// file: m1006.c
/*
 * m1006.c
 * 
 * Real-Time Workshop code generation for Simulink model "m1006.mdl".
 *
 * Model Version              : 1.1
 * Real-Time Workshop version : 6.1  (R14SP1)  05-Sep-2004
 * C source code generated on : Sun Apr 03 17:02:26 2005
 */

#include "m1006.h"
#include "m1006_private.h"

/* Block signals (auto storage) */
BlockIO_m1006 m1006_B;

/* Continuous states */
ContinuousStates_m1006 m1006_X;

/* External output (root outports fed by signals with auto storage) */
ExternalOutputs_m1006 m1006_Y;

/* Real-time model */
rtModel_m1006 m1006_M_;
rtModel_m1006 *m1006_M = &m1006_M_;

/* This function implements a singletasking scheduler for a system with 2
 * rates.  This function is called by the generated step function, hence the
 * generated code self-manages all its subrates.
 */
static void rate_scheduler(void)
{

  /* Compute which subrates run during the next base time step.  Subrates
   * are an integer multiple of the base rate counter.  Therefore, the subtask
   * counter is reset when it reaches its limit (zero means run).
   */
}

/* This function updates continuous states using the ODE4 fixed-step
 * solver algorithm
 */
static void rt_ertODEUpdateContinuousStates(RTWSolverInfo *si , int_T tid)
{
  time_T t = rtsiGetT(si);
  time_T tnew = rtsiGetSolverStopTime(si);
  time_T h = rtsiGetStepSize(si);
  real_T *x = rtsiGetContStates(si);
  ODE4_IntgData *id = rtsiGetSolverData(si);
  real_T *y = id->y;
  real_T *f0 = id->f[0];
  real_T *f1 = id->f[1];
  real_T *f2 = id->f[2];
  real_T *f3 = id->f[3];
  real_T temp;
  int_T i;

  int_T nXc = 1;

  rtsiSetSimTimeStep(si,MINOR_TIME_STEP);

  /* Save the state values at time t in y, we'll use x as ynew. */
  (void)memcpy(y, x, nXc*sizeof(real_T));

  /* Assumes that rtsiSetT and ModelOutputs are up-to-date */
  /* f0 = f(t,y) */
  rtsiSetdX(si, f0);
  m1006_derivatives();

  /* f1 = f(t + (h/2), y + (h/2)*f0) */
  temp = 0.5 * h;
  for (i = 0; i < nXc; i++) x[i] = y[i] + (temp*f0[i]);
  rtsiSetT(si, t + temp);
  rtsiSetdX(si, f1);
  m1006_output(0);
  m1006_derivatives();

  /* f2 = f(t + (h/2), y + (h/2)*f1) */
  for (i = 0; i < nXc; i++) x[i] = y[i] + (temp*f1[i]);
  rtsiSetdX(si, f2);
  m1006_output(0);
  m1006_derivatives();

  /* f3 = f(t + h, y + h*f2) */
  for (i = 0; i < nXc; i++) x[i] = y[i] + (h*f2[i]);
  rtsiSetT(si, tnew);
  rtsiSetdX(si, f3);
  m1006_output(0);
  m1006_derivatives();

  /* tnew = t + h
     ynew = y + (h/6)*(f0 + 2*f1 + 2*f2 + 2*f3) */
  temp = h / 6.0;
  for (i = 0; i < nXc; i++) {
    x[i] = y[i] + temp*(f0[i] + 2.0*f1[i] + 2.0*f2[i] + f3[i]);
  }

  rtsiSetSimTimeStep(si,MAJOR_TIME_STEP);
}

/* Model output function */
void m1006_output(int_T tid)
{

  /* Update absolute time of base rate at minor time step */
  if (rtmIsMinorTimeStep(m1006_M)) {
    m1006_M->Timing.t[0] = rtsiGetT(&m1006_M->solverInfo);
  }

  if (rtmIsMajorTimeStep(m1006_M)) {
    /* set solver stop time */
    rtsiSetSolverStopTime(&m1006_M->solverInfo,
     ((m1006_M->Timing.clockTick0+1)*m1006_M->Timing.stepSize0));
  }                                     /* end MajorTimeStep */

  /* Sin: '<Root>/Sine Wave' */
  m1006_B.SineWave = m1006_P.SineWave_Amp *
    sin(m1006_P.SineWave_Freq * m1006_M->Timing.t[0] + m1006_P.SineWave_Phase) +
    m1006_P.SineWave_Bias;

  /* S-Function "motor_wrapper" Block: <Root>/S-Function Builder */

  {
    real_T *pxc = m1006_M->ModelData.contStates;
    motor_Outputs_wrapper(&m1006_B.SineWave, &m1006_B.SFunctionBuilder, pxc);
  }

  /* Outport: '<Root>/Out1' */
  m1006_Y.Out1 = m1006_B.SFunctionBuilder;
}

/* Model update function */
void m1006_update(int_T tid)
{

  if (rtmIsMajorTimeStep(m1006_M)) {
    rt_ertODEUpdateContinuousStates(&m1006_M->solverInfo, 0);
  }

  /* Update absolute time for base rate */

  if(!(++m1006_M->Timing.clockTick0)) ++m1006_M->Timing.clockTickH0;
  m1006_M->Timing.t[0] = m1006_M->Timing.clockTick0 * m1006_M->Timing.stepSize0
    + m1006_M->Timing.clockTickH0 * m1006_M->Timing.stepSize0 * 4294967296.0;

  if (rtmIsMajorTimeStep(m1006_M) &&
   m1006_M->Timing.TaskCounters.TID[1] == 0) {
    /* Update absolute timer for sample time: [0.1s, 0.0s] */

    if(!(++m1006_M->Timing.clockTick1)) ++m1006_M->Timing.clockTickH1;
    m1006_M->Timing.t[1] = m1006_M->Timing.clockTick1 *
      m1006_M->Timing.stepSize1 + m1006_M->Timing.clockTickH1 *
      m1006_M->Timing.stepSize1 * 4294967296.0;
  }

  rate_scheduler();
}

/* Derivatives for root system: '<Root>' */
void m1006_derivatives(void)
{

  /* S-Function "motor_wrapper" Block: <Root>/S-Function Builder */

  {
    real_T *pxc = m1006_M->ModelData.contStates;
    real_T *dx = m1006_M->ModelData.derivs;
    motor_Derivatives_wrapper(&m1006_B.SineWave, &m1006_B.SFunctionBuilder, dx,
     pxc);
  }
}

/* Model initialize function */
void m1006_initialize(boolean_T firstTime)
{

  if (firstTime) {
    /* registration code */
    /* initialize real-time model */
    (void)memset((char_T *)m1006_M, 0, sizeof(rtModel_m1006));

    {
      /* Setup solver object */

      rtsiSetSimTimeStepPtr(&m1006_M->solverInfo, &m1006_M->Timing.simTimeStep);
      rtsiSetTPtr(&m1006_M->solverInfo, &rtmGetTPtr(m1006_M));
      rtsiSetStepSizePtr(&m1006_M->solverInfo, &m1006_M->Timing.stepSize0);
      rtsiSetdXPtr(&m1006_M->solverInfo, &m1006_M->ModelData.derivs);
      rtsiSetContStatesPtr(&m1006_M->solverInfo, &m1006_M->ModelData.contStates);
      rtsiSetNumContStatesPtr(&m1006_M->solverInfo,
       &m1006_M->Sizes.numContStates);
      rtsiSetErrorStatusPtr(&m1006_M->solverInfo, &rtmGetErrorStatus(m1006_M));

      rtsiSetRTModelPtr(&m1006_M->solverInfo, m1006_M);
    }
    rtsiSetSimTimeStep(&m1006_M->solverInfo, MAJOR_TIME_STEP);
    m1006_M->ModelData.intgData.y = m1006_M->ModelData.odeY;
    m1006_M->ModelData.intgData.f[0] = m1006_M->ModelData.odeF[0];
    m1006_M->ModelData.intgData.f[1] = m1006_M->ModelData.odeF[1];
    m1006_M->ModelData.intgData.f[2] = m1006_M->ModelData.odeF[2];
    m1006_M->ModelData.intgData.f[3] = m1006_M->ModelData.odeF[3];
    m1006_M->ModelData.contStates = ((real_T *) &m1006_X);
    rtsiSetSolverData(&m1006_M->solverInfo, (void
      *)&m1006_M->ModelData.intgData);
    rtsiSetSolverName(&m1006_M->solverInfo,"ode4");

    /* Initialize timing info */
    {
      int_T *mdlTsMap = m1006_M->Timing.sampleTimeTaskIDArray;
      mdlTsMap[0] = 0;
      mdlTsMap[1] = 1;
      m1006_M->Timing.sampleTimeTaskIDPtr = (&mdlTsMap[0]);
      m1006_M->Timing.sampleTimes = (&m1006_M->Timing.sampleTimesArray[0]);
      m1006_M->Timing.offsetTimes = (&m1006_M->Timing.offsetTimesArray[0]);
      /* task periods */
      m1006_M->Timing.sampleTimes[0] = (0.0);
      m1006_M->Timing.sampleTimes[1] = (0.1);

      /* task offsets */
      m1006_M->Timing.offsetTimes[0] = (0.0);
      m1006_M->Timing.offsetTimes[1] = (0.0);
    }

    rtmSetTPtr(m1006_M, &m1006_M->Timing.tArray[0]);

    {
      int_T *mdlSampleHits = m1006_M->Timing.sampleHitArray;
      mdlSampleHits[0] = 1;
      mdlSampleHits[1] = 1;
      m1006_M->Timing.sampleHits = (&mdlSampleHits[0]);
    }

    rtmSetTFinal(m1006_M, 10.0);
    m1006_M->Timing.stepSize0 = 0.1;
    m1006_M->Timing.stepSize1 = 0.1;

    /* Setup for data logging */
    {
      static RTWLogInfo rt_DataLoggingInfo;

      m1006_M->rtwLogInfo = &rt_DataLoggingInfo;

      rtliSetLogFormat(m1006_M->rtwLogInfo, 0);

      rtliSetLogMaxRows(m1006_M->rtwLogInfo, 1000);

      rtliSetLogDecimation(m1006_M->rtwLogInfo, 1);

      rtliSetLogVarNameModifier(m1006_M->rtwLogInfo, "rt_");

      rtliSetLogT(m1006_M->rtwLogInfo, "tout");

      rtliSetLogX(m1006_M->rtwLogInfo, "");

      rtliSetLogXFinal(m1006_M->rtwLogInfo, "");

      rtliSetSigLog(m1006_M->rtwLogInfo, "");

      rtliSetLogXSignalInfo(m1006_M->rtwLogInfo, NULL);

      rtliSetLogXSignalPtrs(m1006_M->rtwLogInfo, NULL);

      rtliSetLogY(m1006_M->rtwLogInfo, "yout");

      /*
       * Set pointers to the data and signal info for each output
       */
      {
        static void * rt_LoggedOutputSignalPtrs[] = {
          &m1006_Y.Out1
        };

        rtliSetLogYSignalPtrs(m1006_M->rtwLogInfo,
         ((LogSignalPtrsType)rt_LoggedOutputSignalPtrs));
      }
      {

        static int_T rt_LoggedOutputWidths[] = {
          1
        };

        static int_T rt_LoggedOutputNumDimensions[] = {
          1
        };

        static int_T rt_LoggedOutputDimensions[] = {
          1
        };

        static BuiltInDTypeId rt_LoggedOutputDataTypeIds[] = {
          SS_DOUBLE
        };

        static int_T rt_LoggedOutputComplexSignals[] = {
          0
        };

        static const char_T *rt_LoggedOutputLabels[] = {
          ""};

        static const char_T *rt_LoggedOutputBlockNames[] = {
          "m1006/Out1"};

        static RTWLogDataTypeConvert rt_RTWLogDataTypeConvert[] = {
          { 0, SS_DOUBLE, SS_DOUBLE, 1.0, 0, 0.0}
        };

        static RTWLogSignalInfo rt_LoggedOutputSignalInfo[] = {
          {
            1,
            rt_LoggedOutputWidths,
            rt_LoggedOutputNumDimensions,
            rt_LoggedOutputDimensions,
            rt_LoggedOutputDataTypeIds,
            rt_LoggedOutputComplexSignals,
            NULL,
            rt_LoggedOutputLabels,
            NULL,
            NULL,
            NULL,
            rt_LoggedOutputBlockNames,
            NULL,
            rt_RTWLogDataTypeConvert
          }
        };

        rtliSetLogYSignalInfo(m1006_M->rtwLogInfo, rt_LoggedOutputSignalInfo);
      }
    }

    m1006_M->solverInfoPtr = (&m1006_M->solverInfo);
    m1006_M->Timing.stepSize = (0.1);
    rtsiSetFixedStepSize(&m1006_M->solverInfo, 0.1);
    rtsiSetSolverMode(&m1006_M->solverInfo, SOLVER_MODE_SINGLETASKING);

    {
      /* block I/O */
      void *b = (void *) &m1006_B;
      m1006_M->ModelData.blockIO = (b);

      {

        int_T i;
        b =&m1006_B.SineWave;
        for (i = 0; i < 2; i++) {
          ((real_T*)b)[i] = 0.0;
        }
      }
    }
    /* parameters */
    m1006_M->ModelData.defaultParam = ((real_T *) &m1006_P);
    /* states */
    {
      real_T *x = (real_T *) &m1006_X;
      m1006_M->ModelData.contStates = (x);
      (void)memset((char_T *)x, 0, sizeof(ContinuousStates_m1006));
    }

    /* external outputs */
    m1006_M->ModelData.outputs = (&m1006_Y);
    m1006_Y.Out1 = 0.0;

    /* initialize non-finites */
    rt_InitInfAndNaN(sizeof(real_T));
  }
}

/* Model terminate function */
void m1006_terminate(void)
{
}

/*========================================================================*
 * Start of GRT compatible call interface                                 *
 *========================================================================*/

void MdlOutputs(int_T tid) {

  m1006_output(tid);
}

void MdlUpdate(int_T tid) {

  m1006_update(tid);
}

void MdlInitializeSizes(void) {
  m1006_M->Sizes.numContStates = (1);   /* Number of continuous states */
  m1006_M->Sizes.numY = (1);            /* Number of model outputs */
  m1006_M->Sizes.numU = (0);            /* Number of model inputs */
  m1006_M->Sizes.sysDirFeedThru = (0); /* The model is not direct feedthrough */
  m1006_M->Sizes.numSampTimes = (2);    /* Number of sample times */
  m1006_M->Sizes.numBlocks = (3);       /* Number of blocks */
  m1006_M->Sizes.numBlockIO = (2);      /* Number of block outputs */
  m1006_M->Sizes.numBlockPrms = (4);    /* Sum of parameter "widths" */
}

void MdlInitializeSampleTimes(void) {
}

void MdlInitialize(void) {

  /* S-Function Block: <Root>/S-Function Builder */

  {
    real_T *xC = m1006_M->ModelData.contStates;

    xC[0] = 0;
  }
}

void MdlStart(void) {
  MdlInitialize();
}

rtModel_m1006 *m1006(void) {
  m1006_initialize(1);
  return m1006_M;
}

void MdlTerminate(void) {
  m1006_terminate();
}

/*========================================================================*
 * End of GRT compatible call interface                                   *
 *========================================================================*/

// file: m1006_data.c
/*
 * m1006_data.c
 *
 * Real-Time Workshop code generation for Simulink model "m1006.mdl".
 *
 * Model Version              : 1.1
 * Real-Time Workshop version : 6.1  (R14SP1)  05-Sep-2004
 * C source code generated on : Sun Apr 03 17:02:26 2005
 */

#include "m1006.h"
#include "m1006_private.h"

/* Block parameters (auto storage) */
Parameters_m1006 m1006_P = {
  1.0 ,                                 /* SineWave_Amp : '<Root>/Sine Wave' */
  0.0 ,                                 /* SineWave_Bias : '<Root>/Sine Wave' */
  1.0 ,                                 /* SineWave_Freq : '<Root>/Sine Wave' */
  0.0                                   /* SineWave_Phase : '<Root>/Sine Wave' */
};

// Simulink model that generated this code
simulink model "m1006"  (Simulink 6.1)
settings: Solver=ode4  StartTime=0.0  StopTime=10.0  FixedStep=0.1  RelTol=1e-3

== system m1006 ==
  S-Function Builder : S-Function  FunctionName=motor  SFunctionModules=motor_wrapper  WizardData=DataTag0  mask(S-Function Builder){}
      mask init:
      | val = [[.9  0.75 0.75 1 1 .9 .9 1]',[1 1 0.75 0.75 .9 .9 1 .9]'];try , sys = get_param(gcb,'SfunBuilderFcnName');if isempty(sys), sys = get_param(gcb,'FunctionName'); end,catch, sys = get_param(gcb,'FunctionName'); end
  Sine Wave : Sin  SampleTime=0
  Out1 : Outport
  wires:
  Sine Wave/1 -> S-Function Builder/1
  S-Function Builder/1 -> Out1/1
